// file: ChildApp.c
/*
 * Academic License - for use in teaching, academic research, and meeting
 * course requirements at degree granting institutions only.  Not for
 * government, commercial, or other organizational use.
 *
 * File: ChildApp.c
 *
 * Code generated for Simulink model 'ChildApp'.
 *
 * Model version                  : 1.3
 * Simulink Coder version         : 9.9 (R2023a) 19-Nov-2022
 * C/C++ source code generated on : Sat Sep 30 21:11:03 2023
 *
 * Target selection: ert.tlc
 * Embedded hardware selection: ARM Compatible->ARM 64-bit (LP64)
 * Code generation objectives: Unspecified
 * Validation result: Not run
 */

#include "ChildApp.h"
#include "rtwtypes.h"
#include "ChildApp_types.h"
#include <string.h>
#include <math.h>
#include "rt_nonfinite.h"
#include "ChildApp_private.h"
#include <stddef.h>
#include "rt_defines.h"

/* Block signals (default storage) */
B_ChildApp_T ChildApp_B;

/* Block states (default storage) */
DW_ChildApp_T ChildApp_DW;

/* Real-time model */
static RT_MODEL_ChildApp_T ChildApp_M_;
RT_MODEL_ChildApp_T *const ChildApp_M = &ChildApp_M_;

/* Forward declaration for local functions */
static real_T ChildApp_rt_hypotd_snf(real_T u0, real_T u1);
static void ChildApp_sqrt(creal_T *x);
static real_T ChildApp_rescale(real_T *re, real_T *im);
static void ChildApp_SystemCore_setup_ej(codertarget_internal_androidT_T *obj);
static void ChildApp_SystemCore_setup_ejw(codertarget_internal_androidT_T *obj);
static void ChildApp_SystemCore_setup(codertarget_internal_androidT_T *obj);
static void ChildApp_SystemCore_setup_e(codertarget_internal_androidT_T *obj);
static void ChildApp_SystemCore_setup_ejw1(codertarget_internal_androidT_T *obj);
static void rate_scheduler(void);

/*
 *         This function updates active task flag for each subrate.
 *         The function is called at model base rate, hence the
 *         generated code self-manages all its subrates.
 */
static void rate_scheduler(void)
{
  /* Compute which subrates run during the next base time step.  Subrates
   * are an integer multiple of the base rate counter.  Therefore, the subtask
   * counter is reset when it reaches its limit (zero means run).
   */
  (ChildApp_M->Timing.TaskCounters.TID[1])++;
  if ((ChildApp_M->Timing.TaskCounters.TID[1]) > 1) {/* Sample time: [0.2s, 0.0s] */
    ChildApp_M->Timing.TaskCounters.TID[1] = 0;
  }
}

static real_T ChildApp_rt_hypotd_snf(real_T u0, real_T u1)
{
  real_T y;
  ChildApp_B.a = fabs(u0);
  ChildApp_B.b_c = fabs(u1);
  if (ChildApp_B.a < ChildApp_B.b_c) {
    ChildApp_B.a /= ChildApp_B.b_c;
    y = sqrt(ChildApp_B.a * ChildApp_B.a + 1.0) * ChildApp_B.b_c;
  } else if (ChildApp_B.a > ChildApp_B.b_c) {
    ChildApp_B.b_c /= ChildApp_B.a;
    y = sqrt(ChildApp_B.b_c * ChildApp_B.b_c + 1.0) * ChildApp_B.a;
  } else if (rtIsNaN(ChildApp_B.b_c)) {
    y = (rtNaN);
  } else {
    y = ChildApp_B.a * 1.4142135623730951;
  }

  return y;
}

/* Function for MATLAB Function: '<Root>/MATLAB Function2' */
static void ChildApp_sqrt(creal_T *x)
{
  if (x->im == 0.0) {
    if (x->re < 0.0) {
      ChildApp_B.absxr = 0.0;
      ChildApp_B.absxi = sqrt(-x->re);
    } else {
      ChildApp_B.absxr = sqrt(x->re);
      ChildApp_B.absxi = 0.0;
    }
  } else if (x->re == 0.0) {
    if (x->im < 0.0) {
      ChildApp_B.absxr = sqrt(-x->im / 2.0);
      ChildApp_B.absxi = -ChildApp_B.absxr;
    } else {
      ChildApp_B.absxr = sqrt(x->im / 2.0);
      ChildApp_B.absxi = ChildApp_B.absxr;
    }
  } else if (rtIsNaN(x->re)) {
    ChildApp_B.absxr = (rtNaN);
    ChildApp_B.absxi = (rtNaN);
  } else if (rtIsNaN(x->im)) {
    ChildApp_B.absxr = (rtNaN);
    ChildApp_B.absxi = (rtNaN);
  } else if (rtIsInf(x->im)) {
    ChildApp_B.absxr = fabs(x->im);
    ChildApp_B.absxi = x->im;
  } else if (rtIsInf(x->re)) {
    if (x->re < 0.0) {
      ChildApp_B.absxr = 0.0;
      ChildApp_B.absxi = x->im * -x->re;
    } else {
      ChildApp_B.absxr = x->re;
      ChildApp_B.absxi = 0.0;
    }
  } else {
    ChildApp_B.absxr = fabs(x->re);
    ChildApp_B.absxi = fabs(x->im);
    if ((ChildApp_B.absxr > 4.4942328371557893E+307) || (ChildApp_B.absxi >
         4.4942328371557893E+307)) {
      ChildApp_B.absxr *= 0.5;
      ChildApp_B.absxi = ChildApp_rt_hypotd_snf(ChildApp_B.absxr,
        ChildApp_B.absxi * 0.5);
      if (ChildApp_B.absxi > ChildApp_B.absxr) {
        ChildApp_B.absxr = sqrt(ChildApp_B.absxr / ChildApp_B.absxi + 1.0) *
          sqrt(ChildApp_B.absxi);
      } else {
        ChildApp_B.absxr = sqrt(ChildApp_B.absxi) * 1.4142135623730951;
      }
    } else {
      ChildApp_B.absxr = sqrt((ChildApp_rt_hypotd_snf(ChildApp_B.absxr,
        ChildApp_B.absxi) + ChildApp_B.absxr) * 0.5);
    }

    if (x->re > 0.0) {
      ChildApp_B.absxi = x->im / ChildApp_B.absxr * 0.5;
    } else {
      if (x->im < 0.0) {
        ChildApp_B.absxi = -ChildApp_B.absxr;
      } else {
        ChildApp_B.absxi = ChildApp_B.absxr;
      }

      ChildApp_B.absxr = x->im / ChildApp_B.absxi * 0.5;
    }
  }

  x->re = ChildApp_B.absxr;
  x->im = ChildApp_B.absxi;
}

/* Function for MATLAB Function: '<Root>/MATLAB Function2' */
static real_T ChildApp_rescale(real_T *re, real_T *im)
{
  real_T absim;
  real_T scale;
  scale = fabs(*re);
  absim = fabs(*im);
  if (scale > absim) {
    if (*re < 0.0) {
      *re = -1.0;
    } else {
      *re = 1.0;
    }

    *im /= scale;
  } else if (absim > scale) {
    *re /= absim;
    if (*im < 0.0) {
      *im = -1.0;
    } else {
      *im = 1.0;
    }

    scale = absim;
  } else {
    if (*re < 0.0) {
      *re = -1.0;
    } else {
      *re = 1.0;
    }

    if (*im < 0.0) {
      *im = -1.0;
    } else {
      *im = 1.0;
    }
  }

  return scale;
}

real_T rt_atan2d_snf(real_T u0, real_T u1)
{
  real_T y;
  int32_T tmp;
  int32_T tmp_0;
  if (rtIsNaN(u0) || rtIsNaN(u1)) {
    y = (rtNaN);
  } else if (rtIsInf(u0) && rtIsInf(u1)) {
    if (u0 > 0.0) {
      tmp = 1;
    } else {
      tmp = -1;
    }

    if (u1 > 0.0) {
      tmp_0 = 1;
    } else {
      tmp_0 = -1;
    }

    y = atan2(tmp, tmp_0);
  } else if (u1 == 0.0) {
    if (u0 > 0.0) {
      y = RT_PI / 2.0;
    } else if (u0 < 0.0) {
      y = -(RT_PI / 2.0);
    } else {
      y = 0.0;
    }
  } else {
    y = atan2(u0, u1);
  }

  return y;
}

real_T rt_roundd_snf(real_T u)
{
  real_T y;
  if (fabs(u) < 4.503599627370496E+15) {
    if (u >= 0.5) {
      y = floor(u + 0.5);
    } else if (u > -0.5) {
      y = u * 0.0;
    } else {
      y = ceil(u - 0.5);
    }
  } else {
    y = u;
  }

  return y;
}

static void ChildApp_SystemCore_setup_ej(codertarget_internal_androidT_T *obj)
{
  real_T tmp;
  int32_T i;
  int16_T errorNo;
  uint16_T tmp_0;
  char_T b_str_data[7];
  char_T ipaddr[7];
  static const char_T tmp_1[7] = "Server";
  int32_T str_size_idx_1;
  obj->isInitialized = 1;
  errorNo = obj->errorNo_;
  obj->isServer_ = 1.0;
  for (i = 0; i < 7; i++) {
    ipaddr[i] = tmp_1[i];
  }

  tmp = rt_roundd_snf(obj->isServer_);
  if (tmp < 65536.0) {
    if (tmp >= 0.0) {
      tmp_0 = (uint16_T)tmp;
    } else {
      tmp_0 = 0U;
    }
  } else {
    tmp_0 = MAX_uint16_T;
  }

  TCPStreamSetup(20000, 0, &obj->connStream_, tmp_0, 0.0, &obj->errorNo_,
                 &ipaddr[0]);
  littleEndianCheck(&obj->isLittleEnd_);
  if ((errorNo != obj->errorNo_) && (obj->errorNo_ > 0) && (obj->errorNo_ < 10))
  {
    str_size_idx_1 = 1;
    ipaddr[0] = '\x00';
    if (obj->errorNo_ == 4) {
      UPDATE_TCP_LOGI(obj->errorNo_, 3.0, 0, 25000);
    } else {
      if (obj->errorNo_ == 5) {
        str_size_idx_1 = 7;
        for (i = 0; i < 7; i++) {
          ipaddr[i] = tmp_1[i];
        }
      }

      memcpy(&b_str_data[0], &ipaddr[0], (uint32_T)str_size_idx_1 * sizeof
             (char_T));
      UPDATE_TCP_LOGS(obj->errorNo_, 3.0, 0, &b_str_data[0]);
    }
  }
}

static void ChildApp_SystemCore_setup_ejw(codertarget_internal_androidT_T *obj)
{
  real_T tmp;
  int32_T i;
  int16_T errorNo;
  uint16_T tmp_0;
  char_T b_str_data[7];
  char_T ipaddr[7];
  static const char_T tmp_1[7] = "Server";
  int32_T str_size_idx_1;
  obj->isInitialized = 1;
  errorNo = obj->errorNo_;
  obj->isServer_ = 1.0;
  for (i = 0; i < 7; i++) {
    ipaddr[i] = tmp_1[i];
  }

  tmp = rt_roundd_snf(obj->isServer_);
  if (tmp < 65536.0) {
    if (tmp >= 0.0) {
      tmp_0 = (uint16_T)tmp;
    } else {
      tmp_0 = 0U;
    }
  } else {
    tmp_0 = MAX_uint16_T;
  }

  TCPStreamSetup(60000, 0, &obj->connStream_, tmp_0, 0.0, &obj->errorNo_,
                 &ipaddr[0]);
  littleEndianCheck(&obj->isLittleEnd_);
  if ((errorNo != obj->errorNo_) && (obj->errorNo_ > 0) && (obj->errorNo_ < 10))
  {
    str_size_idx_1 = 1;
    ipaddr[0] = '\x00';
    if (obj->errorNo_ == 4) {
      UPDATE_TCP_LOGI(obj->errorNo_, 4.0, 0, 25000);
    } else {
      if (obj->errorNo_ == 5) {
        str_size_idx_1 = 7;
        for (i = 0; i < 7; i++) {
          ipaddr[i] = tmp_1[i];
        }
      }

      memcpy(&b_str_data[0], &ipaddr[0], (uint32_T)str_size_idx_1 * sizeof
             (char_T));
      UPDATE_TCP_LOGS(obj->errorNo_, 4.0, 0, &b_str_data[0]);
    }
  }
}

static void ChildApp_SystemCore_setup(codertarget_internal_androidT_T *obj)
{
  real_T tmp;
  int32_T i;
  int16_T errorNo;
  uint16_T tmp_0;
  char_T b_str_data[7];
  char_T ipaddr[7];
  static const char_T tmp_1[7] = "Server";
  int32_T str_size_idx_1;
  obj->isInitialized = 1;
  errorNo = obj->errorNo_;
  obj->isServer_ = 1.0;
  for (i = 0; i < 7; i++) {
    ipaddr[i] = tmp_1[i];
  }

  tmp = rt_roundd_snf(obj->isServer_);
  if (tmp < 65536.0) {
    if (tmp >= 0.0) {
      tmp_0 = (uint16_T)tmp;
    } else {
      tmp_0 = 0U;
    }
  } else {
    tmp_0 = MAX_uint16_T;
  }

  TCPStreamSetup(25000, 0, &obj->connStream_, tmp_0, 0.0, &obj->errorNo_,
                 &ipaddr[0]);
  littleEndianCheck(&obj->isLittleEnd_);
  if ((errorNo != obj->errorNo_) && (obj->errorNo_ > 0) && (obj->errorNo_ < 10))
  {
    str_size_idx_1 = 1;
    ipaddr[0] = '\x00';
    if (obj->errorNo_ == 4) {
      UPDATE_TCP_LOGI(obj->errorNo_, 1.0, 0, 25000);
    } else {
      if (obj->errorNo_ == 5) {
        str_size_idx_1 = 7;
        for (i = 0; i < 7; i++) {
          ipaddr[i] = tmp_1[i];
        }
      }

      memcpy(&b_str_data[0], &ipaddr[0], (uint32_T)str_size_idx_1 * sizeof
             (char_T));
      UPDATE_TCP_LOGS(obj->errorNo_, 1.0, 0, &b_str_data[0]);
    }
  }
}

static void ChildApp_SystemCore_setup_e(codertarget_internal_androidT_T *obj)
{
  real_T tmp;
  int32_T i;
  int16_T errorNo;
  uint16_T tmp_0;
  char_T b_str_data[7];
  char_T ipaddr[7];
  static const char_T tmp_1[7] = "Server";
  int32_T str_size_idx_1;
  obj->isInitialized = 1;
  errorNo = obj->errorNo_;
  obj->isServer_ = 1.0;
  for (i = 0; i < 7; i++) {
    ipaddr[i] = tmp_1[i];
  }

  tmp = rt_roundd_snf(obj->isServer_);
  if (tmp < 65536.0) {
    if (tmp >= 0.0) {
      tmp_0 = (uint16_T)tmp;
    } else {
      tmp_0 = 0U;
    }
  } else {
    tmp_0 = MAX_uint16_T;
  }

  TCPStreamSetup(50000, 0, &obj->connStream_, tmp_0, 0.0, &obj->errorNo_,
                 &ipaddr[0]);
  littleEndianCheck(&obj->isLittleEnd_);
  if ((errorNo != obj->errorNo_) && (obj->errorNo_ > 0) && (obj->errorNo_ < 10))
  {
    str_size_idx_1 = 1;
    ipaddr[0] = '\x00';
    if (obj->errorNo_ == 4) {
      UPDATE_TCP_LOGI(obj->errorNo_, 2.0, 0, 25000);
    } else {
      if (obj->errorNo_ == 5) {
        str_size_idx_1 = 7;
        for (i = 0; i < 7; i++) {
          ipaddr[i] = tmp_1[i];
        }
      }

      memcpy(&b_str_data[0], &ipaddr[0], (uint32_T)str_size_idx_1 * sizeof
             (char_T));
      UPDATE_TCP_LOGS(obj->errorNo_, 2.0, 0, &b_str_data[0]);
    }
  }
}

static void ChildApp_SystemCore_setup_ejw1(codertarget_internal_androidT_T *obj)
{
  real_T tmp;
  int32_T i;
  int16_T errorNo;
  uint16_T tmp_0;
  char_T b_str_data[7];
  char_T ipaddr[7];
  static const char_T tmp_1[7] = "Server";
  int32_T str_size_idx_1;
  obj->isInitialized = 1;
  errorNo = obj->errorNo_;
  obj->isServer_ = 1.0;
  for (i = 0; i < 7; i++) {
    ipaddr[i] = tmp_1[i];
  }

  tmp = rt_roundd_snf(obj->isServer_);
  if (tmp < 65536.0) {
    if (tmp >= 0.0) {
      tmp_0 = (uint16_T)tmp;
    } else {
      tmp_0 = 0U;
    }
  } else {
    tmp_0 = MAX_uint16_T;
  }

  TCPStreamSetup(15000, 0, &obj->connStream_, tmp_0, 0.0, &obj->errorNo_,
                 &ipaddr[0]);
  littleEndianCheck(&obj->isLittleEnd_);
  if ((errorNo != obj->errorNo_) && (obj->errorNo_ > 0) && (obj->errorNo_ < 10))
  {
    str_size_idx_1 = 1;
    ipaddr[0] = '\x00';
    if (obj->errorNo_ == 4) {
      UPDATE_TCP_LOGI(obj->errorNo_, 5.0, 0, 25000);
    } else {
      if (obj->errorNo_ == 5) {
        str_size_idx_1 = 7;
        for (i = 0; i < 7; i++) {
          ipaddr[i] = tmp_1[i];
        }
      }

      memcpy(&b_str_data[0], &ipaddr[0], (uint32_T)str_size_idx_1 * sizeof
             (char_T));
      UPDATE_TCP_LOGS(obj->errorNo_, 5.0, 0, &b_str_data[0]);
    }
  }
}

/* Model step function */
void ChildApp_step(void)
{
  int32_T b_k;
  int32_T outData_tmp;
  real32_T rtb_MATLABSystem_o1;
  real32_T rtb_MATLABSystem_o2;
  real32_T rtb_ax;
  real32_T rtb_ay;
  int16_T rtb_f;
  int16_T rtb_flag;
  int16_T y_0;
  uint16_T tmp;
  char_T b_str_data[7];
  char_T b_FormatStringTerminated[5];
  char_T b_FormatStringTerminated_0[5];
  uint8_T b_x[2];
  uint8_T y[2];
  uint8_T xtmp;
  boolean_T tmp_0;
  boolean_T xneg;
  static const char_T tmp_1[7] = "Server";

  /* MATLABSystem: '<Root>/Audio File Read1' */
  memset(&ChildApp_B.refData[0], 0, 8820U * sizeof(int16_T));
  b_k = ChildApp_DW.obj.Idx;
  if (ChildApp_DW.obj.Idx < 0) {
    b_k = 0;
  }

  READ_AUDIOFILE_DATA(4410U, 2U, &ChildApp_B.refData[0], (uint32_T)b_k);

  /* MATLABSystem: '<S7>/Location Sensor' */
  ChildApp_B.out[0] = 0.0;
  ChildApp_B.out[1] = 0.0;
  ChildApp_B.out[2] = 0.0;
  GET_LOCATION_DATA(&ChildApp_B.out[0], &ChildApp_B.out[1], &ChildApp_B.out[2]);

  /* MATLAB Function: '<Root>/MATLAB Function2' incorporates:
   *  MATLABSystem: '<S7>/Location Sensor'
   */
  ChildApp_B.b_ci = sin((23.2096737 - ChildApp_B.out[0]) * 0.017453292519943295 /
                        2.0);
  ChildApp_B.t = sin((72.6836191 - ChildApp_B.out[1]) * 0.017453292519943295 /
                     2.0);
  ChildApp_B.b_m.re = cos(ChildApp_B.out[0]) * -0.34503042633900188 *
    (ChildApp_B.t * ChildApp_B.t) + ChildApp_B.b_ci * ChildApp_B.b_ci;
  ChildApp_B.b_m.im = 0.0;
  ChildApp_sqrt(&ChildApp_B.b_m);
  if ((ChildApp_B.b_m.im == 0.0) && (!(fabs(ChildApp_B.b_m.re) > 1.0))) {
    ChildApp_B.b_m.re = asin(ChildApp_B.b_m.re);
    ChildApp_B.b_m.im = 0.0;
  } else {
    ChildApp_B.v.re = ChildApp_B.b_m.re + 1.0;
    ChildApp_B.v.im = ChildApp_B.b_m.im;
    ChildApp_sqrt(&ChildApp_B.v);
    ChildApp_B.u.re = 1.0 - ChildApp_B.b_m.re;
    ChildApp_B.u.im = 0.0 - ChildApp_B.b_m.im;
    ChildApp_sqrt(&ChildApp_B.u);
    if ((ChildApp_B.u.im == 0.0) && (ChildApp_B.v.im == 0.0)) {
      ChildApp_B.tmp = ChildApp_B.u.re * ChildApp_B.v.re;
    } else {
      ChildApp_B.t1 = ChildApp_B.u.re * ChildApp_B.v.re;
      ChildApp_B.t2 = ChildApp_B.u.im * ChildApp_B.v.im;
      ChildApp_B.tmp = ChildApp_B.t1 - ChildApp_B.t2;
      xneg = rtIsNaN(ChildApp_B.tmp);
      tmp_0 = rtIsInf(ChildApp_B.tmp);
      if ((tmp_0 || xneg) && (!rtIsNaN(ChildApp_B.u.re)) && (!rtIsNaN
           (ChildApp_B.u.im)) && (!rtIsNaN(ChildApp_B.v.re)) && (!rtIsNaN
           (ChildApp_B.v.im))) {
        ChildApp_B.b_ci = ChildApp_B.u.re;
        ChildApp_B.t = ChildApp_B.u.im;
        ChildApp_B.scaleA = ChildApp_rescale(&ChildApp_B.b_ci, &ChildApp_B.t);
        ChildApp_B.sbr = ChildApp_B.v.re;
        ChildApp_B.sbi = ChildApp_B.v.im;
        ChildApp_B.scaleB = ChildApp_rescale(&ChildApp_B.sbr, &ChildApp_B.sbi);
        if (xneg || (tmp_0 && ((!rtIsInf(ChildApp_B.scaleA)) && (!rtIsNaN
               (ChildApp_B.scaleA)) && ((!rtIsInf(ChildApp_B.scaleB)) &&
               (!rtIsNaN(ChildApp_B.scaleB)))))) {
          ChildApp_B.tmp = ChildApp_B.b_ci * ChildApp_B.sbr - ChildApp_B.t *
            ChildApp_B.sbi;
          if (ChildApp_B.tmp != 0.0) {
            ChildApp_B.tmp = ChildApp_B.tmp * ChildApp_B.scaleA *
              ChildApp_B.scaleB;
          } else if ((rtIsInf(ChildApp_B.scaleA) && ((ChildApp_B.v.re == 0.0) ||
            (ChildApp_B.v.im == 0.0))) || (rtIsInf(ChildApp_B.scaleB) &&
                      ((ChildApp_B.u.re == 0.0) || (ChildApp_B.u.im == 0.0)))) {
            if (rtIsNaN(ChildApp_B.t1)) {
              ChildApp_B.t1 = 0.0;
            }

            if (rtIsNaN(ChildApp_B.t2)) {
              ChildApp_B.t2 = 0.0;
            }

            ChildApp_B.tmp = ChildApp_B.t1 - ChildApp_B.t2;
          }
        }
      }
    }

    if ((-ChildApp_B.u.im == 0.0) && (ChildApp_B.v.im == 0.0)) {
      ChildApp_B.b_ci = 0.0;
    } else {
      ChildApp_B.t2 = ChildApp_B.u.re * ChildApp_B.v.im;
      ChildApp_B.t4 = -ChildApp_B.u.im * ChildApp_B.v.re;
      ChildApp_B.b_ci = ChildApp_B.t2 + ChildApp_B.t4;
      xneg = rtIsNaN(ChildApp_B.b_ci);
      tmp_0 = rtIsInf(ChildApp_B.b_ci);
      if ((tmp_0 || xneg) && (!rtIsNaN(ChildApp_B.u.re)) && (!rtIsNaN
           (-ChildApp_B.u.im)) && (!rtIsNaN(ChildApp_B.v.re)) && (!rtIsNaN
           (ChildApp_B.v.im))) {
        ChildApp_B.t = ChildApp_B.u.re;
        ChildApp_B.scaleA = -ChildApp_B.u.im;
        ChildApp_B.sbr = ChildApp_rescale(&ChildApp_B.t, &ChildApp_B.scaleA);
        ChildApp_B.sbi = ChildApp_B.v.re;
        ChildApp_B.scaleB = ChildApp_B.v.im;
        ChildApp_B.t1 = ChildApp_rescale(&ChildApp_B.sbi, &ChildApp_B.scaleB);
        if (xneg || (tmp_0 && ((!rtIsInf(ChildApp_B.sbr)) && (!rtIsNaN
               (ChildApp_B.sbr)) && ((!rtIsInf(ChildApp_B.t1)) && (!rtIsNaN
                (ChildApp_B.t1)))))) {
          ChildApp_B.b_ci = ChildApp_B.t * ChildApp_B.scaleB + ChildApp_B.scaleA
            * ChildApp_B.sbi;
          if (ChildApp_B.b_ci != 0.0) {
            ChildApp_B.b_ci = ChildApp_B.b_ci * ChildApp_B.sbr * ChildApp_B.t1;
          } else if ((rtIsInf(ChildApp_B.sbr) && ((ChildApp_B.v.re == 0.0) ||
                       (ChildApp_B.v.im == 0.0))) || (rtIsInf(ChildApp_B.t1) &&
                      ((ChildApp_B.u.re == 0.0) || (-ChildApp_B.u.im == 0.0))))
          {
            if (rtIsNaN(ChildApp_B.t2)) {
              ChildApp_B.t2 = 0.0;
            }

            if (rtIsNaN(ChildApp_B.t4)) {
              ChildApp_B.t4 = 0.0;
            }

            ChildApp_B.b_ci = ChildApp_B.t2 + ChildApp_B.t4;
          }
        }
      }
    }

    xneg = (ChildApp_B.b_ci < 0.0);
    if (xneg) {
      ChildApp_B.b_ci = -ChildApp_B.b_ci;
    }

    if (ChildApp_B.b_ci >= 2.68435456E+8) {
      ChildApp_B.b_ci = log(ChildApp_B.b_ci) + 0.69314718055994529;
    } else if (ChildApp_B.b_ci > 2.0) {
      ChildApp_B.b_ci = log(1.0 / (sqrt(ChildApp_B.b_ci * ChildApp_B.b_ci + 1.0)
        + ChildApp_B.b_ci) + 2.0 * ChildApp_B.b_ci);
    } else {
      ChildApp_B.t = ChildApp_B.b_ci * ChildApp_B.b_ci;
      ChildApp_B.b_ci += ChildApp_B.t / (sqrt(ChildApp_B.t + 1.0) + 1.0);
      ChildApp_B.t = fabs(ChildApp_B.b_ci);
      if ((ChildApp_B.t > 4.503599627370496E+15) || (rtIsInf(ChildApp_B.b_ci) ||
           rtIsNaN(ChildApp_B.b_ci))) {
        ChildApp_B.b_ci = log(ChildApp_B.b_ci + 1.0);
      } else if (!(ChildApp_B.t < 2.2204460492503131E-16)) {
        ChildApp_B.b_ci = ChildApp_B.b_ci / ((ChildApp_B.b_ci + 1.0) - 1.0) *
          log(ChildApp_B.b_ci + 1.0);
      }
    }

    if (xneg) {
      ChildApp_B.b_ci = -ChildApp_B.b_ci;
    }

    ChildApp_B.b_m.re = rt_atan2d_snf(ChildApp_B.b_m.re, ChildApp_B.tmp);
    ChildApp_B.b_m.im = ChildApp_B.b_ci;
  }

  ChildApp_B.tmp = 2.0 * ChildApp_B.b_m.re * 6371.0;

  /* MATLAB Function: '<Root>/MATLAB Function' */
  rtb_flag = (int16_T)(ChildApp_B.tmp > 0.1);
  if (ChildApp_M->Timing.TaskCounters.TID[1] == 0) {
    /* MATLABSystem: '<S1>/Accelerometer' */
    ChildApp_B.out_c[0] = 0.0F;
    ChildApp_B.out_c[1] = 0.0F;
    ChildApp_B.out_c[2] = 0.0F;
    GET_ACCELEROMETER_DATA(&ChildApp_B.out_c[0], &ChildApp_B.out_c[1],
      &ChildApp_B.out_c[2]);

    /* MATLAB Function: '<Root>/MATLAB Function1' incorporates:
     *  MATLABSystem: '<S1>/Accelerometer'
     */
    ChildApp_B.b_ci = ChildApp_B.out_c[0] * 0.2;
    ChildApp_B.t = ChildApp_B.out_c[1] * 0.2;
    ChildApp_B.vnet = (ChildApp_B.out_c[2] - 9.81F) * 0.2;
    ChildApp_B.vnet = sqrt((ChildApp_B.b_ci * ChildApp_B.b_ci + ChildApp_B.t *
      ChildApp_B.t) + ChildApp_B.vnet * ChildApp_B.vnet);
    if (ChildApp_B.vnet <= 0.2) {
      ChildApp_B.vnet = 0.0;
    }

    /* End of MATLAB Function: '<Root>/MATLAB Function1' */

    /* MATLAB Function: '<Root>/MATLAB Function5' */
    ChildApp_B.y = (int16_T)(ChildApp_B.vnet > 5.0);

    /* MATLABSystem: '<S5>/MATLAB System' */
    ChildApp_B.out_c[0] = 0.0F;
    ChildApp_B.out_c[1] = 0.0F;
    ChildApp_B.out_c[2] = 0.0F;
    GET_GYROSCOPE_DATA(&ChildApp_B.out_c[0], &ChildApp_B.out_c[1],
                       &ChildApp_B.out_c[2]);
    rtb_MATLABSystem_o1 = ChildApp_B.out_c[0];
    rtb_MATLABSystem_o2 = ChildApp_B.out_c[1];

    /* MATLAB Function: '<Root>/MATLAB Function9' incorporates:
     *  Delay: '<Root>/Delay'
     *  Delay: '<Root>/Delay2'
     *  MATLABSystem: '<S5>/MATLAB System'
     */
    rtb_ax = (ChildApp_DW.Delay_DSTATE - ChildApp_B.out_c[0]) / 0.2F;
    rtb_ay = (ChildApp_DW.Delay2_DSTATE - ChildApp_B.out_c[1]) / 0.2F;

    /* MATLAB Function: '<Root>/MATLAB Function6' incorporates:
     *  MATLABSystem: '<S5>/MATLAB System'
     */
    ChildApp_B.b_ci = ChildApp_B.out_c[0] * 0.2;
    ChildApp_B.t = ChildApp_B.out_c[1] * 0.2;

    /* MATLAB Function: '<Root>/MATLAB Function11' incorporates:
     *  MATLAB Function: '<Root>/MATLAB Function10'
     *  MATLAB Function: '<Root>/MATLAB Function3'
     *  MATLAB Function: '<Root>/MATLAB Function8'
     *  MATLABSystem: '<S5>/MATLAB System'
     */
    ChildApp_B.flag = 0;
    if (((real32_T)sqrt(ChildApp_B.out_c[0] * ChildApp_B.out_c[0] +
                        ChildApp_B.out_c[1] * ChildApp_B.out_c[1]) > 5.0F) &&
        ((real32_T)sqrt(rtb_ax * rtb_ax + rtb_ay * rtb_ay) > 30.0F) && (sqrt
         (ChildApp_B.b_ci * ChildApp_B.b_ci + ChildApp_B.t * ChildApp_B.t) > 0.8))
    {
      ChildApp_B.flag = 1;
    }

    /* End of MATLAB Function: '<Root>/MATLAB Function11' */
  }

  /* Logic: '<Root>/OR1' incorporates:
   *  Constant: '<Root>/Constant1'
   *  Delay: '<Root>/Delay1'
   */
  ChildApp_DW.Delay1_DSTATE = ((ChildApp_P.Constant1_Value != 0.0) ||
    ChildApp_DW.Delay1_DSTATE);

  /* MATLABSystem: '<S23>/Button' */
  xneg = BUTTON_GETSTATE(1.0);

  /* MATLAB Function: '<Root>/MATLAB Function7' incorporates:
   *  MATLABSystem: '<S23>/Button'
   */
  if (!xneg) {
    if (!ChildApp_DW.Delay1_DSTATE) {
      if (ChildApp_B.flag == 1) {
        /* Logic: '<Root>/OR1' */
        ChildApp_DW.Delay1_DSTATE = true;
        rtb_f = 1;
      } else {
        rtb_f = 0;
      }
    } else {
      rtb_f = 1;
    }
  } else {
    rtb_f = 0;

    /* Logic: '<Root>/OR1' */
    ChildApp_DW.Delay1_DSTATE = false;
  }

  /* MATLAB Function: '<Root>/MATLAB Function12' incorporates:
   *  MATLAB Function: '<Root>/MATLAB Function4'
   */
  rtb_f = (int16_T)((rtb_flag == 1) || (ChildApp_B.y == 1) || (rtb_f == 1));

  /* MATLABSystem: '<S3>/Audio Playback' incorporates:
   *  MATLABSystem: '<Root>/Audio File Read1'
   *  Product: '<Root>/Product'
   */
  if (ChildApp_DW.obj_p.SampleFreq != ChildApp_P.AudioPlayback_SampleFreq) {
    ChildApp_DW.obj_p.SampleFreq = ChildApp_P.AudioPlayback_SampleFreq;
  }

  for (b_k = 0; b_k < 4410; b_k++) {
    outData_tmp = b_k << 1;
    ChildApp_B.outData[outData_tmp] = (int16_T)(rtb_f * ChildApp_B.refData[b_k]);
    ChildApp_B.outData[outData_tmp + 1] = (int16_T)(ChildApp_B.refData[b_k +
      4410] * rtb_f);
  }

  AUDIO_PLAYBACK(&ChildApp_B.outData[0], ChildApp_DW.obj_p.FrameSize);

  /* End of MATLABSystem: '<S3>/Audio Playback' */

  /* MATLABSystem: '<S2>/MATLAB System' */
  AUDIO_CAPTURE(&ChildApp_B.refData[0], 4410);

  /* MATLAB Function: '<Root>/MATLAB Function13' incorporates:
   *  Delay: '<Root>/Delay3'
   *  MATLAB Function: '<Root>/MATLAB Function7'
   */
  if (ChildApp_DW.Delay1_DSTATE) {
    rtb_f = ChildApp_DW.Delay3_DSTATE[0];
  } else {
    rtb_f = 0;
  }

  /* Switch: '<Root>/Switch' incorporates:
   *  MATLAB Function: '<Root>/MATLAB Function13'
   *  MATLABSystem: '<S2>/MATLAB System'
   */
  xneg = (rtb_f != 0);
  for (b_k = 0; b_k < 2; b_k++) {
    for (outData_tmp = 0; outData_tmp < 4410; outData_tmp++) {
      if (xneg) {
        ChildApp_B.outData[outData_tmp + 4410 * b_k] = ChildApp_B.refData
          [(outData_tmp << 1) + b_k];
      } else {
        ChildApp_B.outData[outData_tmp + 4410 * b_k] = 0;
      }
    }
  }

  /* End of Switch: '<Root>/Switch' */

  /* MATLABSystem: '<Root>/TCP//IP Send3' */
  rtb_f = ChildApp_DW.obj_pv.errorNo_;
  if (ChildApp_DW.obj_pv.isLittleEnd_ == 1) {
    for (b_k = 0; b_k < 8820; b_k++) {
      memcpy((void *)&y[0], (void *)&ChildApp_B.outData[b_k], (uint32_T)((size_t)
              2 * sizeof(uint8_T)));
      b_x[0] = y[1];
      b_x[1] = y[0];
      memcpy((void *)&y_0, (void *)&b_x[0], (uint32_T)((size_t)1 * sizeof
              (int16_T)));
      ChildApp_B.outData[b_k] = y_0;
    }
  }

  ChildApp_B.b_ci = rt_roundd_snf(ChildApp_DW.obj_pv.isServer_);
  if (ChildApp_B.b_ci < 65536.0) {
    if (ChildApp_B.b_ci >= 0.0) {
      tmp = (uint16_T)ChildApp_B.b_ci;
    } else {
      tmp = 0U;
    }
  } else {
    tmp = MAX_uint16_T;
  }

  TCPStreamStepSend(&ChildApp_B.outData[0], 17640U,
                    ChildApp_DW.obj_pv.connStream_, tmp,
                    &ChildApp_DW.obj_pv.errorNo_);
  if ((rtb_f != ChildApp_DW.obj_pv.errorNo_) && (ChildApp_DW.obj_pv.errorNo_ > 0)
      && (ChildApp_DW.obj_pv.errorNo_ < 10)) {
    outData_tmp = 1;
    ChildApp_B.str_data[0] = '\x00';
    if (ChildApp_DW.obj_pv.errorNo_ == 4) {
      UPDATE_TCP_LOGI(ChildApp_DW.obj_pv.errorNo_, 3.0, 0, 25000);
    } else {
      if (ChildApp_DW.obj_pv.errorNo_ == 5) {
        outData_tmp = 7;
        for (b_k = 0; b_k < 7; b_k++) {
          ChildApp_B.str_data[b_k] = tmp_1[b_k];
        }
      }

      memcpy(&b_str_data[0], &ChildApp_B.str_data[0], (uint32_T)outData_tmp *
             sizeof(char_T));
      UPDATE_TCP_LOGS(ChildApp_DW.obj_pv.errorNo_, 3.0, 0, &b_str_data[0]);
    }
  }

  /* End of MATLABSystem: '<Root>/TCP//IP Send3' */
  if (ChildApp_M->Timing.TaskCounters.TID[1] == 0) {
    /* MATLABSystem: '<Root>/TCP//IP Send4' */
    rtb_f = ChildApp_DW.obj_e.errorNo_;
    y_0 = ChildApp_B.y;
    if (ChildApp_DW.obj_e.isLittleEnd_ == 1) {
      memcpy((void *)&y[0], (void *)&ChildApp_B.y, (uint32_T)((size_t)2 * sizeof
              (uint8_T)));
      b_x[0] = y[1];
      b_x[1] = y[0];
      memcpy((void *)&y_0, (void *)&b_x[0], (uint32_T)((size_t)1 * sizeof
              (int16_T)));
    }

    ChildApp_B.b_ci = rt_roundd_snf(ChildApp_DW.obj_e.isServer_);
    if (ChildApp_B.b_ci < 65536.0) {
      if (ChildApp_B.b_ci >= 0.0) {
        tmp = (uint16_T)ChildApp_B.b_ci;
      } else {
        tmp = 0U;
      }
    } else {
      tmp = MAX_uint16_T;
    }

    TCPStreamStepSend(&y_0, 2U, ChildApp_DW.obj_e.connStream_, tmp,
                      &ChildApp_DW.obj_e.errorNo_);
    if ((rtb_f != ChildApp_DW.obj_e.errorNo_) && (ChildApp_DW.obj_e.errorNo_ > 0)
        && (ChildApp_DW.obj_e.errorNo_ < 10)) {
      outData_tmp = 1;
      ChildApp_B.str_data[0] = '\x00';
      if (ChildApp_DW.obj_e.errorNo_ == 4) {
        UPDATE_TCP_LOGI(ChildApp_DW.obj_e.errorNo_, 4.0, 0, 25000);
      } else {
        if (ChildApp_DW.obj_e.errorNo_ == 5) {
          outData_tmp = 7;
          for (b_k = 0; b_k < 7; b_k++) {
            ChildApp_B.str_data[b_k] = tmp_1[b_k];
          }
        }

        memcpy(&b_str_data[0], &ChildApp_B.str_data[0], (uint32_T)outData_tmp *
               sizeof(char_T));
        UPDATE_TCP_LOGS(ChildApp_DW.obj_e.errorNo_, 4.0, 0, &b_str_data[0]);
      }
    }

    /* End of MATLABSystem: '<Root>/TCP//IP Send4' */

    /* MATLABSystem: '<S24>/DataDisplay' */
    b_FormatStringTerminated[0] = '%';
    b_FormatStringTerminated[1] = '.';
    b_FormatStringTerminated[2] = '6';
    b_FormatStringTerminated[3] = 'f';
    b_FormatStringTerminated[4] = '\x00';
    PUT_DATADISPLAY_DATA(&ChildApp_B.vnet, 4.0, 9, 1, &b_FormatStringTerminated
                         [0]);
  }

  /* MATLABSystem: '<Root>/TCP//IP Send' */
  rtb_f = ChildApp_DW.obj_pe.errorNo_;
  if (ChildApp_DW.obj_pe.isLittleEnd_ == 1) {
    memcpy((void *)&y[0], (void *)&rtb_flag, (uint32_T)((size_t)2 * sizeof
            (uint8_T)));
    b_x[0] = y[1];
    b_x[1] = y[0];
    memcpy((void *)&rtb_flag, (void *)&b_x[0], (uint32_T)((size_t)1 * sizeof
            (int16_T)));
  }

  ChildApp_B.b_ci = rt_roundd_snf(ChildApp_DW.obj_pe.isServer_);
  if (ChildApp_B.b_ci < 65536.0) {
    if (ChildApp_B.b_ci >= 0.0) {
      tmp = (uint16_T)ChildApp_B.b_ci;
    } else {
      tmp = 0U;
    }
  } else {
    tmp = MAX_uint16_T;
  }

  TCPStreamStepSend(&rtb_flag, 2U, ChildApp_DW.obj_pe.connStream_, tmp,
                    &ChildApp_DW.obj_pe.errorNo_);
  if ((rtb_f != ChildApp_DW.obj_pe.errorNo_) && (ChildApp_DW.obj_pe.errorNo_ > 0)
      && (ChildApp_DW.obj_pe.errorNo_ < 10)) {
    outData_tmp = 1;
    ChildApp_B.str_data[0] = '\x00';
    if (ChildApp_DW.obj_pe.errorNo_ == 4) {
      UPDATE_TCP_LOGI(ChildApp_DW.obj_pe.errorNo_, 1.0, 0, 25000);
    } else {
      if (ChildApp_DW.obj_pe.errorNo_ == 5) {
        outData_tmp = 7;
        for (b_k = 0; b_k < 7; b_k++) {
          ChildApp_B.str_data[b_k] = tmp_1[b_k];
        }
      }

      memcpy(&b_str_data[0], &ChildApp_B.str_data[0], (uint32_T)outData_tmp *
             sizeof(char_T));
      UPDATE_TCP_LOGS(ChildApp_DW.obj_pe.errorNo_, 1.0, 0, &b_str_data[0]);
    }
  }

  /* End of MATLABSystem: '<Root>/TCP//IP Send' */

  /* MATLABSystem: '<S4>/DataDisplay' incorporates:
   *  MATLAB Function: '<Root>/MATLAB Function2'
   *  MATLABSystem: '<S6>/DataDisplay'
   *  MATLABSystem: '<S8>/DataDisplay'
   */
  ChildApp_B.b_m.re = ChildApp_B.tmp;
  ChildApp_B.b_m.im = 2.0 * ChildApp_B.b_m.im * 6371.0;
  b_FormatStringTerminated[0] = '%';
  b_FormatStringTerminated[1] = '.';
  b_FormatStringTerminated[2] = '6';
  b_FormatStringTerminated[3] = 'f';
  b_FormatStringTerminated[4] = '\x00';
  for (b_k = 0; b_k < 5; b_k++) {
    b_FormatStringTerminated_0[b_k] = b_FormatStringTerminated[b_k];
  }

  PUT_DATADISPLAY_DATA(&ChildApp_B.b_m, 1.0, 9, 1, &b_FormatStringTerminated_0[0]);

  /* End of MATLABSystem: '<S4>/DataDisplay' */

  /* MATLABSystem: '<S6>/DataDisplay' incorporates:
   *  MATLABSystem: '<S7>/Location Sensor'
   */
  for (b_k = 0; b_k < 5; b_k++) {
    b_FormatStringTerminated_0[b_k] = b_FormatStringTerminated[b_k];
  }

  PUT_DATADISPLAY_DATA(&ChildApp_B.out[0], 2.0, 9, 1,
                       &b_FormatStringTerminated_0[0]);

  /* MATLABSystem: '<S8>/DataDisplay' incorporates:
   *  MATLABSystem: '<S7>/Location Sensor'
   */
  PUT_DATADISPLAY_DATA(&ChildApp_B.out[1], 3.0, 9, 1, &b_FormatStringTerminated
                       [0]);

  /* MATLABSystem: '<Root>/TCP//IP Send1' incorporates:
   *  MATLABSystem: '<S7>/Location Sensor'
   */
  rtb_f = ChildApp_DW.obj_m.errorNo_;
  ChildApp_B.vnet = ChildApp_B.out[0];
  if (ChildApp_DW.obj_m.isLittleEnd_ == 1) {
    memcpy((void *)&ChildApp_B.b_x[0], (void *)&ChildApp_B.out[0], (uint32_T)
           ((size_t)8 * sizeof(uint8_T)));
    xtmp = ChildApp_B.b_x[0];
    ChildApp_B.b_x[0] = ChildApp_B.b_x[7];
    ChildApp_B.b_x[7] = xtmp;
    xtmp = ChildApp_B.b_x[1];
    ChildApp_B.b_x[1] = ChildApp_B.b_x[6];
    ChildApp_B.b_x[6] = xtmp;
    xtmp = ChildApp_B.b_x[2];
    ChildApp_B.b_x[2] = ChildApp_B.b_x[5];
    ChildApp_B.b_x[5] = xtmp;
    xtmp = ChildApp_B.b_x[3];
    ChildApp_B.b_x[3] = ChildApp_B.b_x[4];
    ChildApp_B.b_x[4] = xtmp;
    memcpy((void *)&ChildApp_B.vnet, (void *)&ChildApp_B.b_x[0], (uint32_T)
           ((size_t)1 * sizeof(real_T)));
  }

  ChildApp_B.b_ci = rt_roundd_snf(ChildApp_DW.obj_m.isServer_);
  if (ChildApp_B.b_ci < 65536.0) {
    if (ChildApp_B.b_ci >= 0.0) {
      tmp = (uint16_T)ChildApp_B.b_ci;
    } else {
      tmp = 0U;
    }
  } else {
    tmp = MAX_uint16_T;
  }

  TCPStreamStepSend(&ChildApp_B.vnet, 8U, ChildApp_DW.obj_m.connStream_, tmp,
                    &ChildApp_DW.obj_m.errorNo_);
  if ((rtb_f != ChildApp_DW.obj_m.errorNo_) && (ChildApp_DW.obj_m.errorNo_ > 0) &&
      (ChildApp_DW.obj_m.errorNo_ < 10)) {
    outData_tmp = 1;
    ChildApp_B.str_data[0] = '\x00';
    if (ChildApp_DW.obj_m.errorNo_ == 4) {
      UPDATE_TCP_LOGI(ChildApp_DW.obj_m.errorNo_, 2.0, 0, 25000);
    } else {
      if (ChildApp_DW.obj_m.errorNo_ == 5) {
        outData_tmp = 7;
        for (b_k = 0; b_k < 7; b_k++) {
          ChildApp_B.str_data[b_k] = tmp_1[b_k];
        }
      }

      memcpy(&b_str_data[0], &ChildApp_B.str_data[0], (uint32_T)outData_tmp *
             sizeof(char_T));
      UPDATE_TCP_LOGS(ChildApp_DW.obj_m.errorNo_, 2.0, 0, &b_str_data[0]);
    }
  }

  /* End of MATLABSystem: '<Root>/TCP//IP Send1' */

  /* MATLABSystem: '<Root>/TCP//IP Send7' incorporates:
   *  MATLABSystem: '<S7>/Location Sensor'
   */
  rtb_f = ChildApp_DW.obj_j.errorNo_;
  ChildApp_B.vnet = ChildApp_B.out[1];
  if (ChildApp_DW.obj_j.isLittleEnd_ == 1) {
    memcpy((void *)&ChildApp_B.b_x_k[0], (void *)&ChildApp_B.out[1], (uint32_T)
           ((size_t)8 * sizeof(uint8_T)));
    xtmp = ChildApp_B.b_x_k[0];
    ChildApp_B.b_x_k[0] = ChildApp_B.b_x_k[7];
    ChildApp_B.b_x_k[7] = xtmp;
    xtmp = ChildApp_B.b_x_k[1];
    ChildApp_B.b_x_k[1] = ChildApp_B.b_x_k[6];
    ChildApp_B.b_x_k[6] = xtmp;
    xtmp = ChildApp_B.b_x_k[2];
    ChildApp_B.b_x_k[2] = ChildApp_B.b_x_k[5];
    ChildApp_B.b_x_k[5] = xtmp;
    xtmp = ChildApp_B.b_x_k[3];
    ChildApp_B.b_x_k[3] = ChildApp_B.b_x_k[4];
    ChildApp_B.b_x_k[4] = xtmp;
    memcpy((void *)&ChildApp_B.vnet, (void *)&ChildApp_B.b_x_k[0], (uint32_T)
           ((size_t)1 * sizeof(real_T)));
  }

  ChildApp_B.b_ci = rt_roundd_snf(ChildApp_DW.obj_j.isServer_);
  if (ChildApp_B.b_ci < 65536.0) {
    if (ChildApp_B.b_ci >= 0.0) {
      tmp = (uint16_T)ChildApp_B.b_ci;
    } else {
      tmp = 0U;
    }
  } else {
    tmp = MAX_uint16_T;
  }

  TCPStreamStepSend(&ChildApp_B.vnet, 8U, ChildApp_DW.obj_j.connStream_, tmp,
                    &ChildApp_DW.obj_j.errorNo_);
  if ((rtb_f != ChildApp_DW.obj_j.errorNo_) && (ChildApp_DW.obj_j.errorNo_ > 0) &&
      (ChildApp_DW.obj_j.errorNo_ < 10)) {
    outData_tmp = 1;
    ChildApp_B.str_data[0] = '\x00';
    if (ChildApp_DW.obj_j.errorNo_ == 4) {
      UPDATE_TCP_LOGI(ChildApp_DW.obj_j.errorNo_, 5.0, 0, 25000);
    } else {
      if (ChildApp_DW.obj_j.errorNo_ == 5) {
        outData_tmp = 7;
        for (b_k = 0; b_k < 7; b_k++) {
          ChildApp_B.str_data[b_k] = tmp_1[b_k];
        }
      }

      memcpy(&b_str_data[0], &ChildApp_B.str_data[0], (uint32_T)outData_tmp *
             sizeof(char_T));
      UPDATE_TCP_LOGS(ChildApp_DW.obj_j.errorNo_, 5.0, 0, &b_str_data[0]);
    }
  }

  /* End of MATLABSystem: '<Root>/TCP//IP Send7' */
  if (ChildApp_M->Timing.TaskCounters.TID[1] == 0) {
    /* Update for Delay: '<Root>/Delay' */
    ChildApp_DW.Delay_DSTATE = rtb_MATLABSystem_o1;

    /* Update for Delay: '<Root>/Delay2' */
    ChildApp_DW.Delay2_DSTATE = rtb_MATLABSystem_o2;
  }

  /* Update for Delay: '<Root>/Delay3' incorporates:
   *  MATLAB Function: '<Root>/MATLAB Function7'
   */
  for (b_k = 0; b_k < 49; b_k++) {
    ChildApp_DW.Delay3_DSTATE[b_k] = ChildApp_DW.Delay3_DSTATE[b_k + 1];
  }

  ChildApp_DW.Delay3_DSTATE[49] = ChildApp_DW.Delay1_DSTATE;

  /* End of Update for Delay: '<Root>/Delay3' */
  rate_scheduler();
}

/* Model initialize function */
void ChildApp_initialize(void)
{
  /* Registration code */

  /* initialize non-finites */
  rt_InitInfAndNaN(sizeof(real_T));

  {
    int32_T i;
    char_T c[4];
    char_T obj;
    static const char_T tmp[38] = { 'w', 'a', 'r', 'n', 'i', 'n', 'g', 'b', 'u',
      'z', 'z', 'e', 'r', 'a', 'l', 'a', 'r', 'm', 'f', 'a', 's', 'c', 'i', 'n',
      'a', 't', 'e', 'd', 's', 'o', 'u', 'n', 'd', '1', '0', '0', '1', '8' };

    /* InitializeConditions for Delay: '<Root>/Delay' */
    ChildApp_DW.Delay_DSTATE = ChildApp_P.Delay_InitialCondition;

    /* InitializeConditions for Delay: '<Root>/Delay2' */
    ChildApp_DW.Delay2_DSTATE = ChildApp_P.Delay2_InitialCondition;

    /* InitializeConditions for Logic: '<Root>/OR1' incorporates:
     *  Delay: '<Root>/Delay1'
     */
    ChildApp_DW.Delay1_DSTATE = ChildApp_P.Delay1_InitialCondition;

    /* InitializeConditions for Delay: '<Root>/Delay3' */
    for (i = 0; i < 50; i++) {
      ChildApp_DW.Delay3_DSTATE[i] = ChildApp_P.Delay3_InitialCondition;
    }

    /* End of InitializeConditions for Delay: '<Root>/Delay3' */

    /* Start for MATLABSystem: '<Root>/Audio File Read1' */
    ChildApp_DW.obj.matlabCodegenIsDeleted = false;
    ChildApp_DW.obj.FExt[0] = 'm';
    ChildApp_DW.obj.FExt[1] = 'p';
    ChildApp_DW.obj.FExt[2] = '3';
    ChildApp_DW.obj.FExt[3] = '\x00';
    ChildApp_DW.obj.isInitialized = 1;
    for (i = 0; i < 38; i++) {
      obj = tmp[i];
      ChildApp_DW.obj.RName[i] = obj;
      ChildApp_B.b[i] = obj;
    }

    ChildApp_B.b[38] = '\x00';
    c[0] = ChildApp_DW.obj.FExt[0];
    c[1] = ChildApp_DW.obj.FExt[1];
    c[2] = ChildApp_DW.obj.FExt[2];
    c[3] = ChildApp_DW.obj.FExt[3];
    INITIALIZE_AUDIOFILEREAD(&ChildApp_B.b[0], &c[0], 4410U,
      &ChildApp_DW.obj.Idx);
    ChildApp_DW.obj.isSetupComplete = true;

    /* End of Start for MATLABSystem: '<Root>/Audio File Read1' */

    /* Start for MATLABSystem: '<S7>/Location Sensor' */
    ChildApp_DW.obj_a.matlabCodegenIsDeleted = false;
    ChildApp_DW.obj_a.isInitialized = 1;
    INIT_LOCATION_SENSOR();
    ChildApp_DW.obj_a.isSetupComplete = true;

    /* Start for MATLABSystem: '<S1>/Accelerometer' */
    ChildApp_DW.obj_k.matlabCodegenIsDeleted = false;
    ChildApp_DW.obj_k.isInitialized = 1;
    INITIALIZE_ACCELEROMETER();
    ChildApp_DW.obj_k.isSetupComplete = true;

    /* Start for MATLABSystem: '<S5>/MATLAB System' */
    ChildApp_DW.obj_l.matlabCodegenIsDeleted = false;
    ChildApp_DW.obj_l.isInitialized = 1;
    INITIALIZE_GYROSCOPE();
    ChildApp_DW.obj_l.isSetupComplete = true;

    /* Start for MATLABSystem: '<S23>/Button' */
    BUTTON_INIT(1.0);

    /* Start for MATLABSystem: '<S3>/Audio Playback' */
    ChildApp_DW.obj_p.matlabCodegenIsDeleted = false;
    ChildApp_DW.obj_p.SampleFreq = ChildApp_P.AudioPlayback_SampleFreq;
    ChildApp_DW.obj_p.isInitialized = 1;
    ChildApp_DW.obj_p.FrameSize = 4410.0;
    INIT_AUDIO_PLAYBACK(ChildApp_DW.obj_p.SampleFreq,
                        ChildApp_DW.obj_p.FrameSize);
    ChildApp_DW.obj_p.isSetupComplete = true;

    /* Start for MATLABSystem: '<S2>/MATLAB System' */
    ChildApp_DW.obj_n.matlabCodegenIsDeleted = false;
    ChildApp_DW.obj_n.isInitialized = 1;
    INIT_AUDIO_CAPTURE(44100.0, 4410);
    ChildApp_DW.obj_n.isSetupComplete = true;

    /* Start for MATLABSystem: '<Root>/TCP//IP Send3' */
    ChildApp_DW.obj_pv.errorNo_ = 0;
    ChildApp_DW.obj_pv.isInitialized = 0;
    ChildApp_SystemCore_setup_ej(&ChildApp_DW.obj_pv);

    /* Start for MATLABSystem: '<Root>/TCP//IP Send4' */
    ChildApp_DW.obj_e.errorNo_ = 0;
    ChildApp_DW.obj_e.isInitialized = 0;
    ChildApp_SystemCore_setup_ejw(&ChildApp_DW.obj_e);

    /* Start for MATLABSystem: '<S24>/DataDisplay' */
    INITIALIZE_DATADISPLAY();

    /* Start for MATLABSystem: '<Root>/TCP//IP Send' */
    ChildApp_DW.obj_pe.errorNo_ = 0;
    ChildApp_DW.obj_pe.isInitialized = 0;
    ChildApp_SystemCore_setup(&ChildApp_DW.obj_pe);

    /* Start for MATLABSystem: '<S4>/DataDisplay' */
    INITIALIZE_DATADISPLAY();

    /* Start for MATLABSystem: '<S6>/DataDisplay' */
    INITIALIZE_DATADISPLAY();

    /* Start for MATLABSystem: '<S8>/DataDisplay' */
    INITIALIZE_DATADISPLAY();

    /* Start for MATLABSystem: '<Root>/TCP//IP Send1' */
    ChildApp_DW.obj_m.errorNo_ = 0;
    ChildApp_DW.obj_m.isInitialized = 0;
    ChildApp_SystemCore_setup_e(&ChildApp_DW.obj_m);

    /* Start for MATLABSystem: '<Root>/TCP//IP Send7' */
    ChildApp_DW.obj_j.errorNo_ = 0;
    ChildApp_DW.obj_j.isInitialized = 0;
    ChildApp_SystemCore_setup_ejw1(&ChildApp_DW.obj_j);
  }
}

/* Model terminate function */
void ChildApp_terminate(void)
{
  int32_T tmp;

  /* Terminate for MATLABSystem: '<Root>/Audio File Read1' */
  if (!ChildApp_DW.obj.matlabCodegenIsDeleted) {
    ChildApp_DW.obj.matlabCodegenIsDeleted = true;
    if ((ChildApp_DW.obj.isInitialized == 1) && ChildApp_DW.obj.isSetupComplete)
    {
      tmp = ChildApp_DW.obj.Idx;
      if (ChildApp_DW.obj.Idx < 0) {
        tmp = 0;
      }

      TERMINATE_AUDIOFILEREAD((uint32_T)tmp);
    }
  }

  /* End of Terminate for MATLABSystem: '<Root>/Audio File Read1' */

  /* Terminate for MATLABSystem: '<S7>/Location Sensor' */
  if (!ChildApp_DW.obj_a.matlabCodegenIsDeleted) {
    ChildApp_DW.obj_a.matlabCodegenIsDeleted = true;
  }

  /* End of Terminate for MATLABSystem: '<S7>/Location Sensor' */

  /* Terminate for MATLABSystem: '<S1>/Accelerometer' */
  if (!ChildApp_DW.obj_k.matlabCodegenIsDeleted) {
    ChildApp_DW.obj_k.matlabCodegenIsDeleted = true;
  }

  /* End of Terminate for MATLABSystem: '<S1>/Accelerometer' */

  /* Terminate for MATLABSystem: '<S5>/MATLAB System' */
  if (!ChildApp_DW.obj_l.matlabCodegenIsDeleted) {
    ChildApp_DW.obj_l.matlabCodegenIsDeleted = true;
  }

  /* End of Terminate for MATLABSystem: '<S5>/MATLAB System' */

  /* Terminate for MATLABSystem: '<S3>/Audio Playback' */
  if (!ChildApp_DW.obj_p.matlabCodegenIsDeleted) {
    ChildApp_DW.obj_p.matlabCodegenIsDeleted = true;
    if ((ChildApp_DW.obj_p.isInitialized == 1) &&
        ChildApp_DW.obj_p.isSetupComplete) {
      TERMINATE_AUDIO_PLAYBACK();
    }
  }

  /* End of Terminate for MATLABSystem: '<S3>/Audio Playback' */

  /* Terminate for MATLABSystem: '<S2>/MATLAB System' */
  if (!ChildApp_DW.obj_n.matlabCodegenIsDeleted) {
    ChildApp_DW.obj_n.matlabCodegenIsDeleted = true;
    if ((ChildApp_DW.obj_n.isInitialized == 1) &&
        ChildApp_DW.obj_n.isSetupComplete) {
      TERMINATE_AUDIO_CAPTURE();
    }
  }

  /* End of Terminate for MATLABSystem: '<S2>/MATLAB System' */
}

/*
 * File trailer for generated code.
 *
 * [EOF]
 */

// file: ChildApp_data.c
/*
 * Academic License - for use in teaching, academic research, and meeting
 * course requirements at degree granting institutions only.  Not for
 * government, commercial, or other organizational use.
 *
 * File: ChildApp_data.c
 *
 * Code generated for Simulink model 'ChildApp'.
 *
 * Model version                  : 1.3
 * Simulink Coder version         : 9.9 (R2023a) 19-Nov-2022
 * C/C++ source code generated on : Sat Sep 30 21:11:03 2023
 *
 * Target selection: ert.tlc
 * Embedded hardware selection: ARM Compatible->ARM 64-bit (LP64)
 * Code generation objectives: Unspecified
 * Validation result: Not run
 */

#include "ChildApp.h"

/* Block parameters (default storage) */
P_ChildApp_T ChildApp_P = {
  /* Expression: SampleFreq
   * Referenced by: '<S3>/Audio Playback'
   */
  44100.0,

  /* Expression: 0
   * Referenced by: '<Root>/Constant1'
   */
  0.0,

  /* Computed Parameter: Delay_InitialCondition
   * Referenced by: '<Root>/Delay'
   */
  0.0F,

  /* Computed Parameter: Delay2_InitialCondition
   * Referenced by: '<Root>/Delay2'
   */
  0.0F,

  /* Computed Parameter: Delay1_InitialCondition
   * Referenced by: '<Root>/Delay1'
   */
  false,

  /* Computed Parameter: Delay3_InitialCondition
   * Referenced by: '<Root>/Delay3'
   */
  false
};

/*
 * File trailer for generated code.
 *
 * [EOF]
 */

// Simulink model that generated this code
simulink model "ChildApp"  (R2023a)
settings: Solver=FixedStepAuto  StartTime=0.0  StopTime=10  RelTol=1e-3
libraries: androidcommunicationlib x6, androiduilib x5, androidaudiovideolib x4, androidsensorlib x3

== system ChildApp ==
  Accelerometer : androidsensorlib/Accelerometer  OutputVector=off  SampleTime=0.2  BlockPlatform=Android
  Audio Capture : androidaudiovideolib/Audio Capture  SampleFreq=44100  FrameSize=4410  SampleTime=0.1  SimulateUsing=Code generation  DeviceStr=0  QueueDuration=0  BlockPlatform=Android  AudioSamplingFreq=44100
  Audio File Read1 : androidaudiovideolib/Audio File Read  FileName=C:\Users\Hitesh\Downloads\warning-buzzer-alarm-fascinatedsound-1-00-18.mp3  FrameSize=4410
  Audio Playback : androidaudiovideolib/Audio Playback  SampleFreq=44100  AudioSamplingFreq=44100  SampleTime=0.1  DeviceStr=0  QueueDuration=0  BlockPlatform=Android
  Camera : androidaudiovideolib/Camera  Commented=on  CameraLocation=Back  CameraResolutions=Back - 320x240  Width=320  Height=240  SampleTime=2  BlockPlatform=Android
  Constant1 : Constant  Value=0  OutDataTypeStr=double
  Delay : Delay  DelayLength=1
  Delay1 : Delay  DelayLength=1  InitialCondition=0
  Delay2 : Delay  DelayLength=1
  Delay3 : Delay  DelayLength=50  InitialCondition=0
  Distance : androiduilib/Data Display  DataDisplayId=ChildApp/Distance  Format=Float  Precision=6  SimulateUsing=Code generation  blockPlatform=Android
  Gyroscope : androidsensorlib/Gyroscope  OutputVector=off  SampleTime=0.2  BlockPlatform=Android
  Latitude : androiduilib/Data Display  DataDisplayId=ChildApp/Latitude  Format=Float  Precision=6  SimulateUsing=Code generation  blockPlatform=Android
  Location Sensor : androidsensorlib/Location Sensor  OutputVector=off  SampleTime=0.1  BlockPlatform=Android
  Longitude : androiduilib/Data Display  DataDisplayId=ChildApp/Longitude  Format=Float  Precision=6  SimulateUsing=Code generation  blockPlatform=Android
  MATLAB Function : MATLAB Function  TreatAsAtomicUnit=on
  MATLAB Function1 : MATLAB Function  TreatAsAtomicUnit=on
  MATLAB Function10 : MATLAB Function  TreatAsAtomicUnit=on
  MATLAB Function11 : MATLAB Function  TreatAsAtomicUnit=on
  MATLAB Function12 : MATLAB Function  TreatAsAtomicUnit=on
  MATLAB Function13 : MATLAB Function  TreatAsAtomicUnit=on
  MATLAB Function2 : MATLAB Function  TreatAsAtomicUnit=on
  MATLAB Function3 : MATLAB Function  TreatAsAtomicUnit=on
  MATLAB Function4 : MATLAB Function  TreatAsAtomicUnit=on
  MATLAB Function5 : MATLAB Function  TreatAsAtomicUnit=on
  MATLAB Function6 : MATLAB Function  TreatAsAtomicUnit=on
  MATLAB Function7 : MATLAB Function  TreatAsAtomicUnit=on
  MATLAB Function8 : MATLAB Function  TreatAsAtomicUnit=on
  MATLAB Function9 : MATLAB Function  TreatAsAtomicUnit=on
  Mux : Mux  Commented=on  Inputs=3
  OR1 : Logic  Operator=OR  IconShape=distinctive  AllPortsSameDT=off  OutDataTypeStr=boolean
  Press if you are fine. : androiduilib/Button  ButtonState=Not pressed  ButtonId=ChildApp/Press_if_you_are_fine.  State=off  SampleTime=0.1  BlockPlatform=Android
  Product : Product  InputSameDT=on  OutDataTypeStr=Inherit: Same as first input
  Reshape1 : Reshape  Commented=on  OutputDimensionality=Customize  OutputDimensions=[320*240,1]
  Reshape2 : Reshape  Commented=on  OutputDimensionality=Customize  OutputDimensions=[320*240,1]
  Reshape3 : Reshape  Commented=on  OutputDimensionality=Customize  OutputDimensions=[320*240,1]
  Reshape4 : Reshape  OutputDimensionality=Customize  OutputDimensions=[8820,1]
  Speed : androiduilib/Data Display  DataDisplayId=ChildApp/Speed  Format=Float  Precision=6  SimulateUsing=Code generation  blockPlatform=Android
  Switch : Switch  Criteria=u2 ~= 0  OutDataTypeStr=int16  SaturateOnIntegerOverflow=off  InputSameDT=off
  TCP/IP Send : androidcommunicationlib/TCP//IP Send  TCPSendId=ChildApp/TCP//IP_Send  Mode_=Server  LocalServerPort_=25000  RemoteAddr_=137.158.24.15  RemoteServerPort_=38000  ClientPortBindingSelection_=off  ClientPortToBind_=35000  BlockingMode_=off  BlockTimeout_=0.1
  TCP/IP Send1 : androidcommunicationlib/TCP//IP Send  TCPSendId=ChildApp/TCP//IP_Send1  Mode_=Server  LocalServerPort_=50000  RemoteAddr_=127.0.0.1  RemoteServerPort_=25000  ClientPortBindingSelection_=off  ClientPortToBind_=35000  BlockingMode_=off  BlockTimeout_=0.1
  TCP/IP Send2 : androidcommunicationlib/TCP//IP Send  Commented=on  TCPSendId=ChildApp/TCP//IP_Send2  Mode_=Server  LocalServerPort_=45000  RemoteAddr_=137.158.24.15  RemoteServerPort_=38000  ClientPortBindingSelection_=off  ClientPortToBind_=35000  BlockingMode_=off  BlockTimeout_=0.1
  TCP/IP Send3 : androidcommunicationlib/TCP//IP Send  TCPSendId=ChildApp/TCP//IP_Send3  Mode_=Server  LocalServerPort_=20000  RemoteAddr_=137.158.24.15  RemoteServerPort_=38000  ClientPortBindingSelection_=off  ClientPortToBind_=35000  BlockingMode_=off  BlockTimeout_=0.1
  TCP/IP Send4 : androidcommunicationlib/TCP//IP Send  TCPSendId=ChildApp/TCP//IP_Send4  Mode_=Server  LocalServerPort_=60000  RemoteAddr_=137.158.24.15  RemoteServerPort_=38000  ClientPortBindingSelection_=off  ClientPortToBind_=35000  BlockingMode_=off  BlockTimeout_=0.1
  TCP/IP Send7 : androidcommunicationlib/TCP//IP Send  TCPSendId=ChildApp/TCP//IP_Send7  Mode_=Server  LocalServerPort_=15000  RemoteAddr_=127.0.0.1  RemoteServerPort_=25000  ClientPortBindingSelection_=off  ClientPortToBind_=35000  BlockingMode_=off  BlockTimeout_=0.1
  Terminator2 : Terminator
  Terminator3 : Terminator
  wires:
  Gyroscope/1 -> MATLAB Function6/1(wx), Delay/1, MATLAB Function9/1(wx1), MATLAB Function3/1(wx)
  Gyroscope/2 -> MATLAB Function6/2(wy), Delay2/1, MATLAB Function9/2(wy1), MATLAB Function3/2(wy)
  Delay2/1 -> MATLAB Function9/4(wy2)
  Product/1 -> Audio Playback/1
  MATLAB Function3/1(wnet) -> MATLAB Function11/1(wnet)
  Delay1/1 -> OR1/2
  Delay/1 -> MATLAB Function9/3(wx2)
  MATLAB Function6/1(thetx) -> MATLAB Function8/1(thetx)
  MATLAB Function6/2(thety) -> MATLAB Function8/2(thety)
  Location Sensor/2 -> MATLAB Function2/2(lon1), TCP/IP Send7/1, Longitude/1
  Accelerometer/1 -> MATLAB Function1/1(ax)
  Accelerometer/2 -> MATLAB Function1/2(ay)
  MATLAB Function5/1(y) -> MATLAB Function4/2(b), TCP/IP Send4/1
  Accelerometer/3 -> MATLAB Function1/3(az)
  MATLAB Function9/2(ay) -> MATLAB Function10/2(ay)
  MATLAB Function9/1(ax) -> MATLAB Function10/1(ax)
  MATLAB Function8/1(thetnet) -> MATLAB Function11/3(thetnet)
  Constant1/1 -> OR1/1
  MATLAB Function2/1(d) -> MATLAB Function/1(d), Distance/1
  MATLAB Function11/1(flag) -> MATLAB Function7/1(f0)
  MATLAB Function1/1(vnet) -> Speed/1, MATLAB Function5/1(v)
  MATLAB Function10/1(anet) -> MATLAB Function11/2(anet)
  Press if you are fine./1 -> MATLAB Function7/3(b)
  OR1/1 -> MATLAB Function7/2("k ")
  MATLAB Function7/1(f) -> MATLAB Function12/2(a)
  MATLAB Function/1(flag) -> MATLAB Function4/1(a), TCP/IP Send/1
  MATLAB Function4/1(y) -> MATLAB Function12/1(b)
  MATLAB Function12/1(y) -> Product/1
  Audio File Read1/1 -> Product/2
  Gyroscope/3 -> Terminator2/1
  Location Sensor/3 -> Terminator3/1
  Audio Capture/1 -> Switch/1
  Switch/1 -> Reshape4/1
  Camera/1 -> Reshape1/1
  Camera/3 -> Reshape3/1
  Camera/2 -> Reshape2/1
  Reshape4/1 -> TCP/IP Send3/1
  Mux/1 -> TCP/IP Send2/1
  Reshape1/1 -> Mux/1
  Reshape2/1 -> Mux/2
  Reshape3/1 -> Mux/3
  Delay3/1 -> MATLAB Function13/2(d)
  MATLAB Function13/1(y) -> Switch/2
  MATLAB Function7/2(k) -> MATLAB Function13/1(c), Delay3/1, Delay1/1
  Location Sensor/1 -> MATLAB Function2/1(lat1), TCP/IP Send1/1, Latitude/1

== matlab function ChildApp/MATLAB Function8 ==
function thetnet = mag(thetx,thety)
    thetnet = sqrt(thetx^2+thety^2);
end

== matlab function ChildApp/MATLAB Function9 ==
function [ax,ay] = integrateAcceleration(wx1,wy1,wx2,wy2)
    dt=0.2;
    ax=(wx2-wx1)/dt;
    ay=(wy2-wy1)/dt;
end

== matlab function ChildApp/MATLAB Function12 ==
function y = OR(b,a)
    if(b == 1 || a == 1)
        y = int16(1);
    else
        y = int16(0);
    end
end

== matlab function ChildApp/MATLAB Function13 ==
function y = fcn(c,d)
    if(c == 1)
        if(d == 1)
            y = int16(1);
        else
            y = int16(0);
        end
    else
        y = int16(0);
    end
end

== matlab function ChildApp/MATLAB Function1 ==
function vnet = speed(ax,ay,az)
    dt = 0.2;
    vx = double(ax)*dt;
    vy = double(ay)*dt;
    vz = double(az-9.81)*dt;
    vnet = sqrt(vx^2+vy^2+vz^2);
    if( vnet<= 0.2)
        vnet = 0;
    end
end

== matlab function ChildApp/MATLAB Function2 ==
function d = DistanceFromLatLonInKm(lat1,lon1)
    R = 6371;
    lat2 = 23.2096737;
    lon2 = 72.6836191;
    % Haversine formula
    dlat = deg2rad(lat2-lat1);
    dlon = deg2rad(lon2-lon1); 
    a = sin(dlat/2)^2 + cos(lat1)* cos(lat2) * sin(dlon/2)^2;
    c = 2 * asin(sqrt(complex(a)));  
    d = R * c; % in km
end

== matlab function ChildApp/MATLAB Function ==
function flag = is_out_of_boundary(d)
    if(d > 0.1)
        flag = int16(1);
    else 
        flag = int16(0);
    end
end

== matlab function ChildApp/MATLAB Function10 ==
function anet = mag(ax,ay)
    anet = sqrt(ax^2+ay^2);
end

== matlab function ChildApp/MATLAB Function4 ==
function y = OR(a,b)
    if(a == 1 || b == 1)
        y = int16(1);
    else 
        y = int16(0);
    end
end

== matlab function ChildApp/MATLAB Function5 ==
function y = is_overspeeding(v)
    if(v>5)
        y = int16(1);
    else
        y = int16(0);
    end

end

== matlab function ChildApp/MATLAB Function11 ==
function flag = check(wnet,anet,thetnet)
    flag=int16(0);
    if(wnet > 5)
        if(anet > 30 && thetnet > 0.8)
            flag=int16(1);          
        end
    end
end

== matlab function ChildApp/MATLAB Function3 ==
function wnet = mag(wx,wy)
    wnet = sqrt(wx^2+wy^2);
end

== matlab function ChildApp/MATLAB Function6 ==
function [thetx,thety] = integrateAcceleration(wx,wy)
    dt=0.2;
    thetx =double(wx) * dt;
    thety =double(wy) * dt;
end

== matlab function ChildApp/MATLAB Function7 ==
function [f,k]= check_if_injured_or_not(f0,k,b)
    if(b == false)
        if(k == false)
            if(f0 == 1)
                k = true;
                f = int16(1);
                return;
            end
            f = int16(0);
        elseif(k == true)
            f = int16(1);
        else
            f = int16(0);
        end
    else
        f = int16(0);
        k = false;
    end
end
